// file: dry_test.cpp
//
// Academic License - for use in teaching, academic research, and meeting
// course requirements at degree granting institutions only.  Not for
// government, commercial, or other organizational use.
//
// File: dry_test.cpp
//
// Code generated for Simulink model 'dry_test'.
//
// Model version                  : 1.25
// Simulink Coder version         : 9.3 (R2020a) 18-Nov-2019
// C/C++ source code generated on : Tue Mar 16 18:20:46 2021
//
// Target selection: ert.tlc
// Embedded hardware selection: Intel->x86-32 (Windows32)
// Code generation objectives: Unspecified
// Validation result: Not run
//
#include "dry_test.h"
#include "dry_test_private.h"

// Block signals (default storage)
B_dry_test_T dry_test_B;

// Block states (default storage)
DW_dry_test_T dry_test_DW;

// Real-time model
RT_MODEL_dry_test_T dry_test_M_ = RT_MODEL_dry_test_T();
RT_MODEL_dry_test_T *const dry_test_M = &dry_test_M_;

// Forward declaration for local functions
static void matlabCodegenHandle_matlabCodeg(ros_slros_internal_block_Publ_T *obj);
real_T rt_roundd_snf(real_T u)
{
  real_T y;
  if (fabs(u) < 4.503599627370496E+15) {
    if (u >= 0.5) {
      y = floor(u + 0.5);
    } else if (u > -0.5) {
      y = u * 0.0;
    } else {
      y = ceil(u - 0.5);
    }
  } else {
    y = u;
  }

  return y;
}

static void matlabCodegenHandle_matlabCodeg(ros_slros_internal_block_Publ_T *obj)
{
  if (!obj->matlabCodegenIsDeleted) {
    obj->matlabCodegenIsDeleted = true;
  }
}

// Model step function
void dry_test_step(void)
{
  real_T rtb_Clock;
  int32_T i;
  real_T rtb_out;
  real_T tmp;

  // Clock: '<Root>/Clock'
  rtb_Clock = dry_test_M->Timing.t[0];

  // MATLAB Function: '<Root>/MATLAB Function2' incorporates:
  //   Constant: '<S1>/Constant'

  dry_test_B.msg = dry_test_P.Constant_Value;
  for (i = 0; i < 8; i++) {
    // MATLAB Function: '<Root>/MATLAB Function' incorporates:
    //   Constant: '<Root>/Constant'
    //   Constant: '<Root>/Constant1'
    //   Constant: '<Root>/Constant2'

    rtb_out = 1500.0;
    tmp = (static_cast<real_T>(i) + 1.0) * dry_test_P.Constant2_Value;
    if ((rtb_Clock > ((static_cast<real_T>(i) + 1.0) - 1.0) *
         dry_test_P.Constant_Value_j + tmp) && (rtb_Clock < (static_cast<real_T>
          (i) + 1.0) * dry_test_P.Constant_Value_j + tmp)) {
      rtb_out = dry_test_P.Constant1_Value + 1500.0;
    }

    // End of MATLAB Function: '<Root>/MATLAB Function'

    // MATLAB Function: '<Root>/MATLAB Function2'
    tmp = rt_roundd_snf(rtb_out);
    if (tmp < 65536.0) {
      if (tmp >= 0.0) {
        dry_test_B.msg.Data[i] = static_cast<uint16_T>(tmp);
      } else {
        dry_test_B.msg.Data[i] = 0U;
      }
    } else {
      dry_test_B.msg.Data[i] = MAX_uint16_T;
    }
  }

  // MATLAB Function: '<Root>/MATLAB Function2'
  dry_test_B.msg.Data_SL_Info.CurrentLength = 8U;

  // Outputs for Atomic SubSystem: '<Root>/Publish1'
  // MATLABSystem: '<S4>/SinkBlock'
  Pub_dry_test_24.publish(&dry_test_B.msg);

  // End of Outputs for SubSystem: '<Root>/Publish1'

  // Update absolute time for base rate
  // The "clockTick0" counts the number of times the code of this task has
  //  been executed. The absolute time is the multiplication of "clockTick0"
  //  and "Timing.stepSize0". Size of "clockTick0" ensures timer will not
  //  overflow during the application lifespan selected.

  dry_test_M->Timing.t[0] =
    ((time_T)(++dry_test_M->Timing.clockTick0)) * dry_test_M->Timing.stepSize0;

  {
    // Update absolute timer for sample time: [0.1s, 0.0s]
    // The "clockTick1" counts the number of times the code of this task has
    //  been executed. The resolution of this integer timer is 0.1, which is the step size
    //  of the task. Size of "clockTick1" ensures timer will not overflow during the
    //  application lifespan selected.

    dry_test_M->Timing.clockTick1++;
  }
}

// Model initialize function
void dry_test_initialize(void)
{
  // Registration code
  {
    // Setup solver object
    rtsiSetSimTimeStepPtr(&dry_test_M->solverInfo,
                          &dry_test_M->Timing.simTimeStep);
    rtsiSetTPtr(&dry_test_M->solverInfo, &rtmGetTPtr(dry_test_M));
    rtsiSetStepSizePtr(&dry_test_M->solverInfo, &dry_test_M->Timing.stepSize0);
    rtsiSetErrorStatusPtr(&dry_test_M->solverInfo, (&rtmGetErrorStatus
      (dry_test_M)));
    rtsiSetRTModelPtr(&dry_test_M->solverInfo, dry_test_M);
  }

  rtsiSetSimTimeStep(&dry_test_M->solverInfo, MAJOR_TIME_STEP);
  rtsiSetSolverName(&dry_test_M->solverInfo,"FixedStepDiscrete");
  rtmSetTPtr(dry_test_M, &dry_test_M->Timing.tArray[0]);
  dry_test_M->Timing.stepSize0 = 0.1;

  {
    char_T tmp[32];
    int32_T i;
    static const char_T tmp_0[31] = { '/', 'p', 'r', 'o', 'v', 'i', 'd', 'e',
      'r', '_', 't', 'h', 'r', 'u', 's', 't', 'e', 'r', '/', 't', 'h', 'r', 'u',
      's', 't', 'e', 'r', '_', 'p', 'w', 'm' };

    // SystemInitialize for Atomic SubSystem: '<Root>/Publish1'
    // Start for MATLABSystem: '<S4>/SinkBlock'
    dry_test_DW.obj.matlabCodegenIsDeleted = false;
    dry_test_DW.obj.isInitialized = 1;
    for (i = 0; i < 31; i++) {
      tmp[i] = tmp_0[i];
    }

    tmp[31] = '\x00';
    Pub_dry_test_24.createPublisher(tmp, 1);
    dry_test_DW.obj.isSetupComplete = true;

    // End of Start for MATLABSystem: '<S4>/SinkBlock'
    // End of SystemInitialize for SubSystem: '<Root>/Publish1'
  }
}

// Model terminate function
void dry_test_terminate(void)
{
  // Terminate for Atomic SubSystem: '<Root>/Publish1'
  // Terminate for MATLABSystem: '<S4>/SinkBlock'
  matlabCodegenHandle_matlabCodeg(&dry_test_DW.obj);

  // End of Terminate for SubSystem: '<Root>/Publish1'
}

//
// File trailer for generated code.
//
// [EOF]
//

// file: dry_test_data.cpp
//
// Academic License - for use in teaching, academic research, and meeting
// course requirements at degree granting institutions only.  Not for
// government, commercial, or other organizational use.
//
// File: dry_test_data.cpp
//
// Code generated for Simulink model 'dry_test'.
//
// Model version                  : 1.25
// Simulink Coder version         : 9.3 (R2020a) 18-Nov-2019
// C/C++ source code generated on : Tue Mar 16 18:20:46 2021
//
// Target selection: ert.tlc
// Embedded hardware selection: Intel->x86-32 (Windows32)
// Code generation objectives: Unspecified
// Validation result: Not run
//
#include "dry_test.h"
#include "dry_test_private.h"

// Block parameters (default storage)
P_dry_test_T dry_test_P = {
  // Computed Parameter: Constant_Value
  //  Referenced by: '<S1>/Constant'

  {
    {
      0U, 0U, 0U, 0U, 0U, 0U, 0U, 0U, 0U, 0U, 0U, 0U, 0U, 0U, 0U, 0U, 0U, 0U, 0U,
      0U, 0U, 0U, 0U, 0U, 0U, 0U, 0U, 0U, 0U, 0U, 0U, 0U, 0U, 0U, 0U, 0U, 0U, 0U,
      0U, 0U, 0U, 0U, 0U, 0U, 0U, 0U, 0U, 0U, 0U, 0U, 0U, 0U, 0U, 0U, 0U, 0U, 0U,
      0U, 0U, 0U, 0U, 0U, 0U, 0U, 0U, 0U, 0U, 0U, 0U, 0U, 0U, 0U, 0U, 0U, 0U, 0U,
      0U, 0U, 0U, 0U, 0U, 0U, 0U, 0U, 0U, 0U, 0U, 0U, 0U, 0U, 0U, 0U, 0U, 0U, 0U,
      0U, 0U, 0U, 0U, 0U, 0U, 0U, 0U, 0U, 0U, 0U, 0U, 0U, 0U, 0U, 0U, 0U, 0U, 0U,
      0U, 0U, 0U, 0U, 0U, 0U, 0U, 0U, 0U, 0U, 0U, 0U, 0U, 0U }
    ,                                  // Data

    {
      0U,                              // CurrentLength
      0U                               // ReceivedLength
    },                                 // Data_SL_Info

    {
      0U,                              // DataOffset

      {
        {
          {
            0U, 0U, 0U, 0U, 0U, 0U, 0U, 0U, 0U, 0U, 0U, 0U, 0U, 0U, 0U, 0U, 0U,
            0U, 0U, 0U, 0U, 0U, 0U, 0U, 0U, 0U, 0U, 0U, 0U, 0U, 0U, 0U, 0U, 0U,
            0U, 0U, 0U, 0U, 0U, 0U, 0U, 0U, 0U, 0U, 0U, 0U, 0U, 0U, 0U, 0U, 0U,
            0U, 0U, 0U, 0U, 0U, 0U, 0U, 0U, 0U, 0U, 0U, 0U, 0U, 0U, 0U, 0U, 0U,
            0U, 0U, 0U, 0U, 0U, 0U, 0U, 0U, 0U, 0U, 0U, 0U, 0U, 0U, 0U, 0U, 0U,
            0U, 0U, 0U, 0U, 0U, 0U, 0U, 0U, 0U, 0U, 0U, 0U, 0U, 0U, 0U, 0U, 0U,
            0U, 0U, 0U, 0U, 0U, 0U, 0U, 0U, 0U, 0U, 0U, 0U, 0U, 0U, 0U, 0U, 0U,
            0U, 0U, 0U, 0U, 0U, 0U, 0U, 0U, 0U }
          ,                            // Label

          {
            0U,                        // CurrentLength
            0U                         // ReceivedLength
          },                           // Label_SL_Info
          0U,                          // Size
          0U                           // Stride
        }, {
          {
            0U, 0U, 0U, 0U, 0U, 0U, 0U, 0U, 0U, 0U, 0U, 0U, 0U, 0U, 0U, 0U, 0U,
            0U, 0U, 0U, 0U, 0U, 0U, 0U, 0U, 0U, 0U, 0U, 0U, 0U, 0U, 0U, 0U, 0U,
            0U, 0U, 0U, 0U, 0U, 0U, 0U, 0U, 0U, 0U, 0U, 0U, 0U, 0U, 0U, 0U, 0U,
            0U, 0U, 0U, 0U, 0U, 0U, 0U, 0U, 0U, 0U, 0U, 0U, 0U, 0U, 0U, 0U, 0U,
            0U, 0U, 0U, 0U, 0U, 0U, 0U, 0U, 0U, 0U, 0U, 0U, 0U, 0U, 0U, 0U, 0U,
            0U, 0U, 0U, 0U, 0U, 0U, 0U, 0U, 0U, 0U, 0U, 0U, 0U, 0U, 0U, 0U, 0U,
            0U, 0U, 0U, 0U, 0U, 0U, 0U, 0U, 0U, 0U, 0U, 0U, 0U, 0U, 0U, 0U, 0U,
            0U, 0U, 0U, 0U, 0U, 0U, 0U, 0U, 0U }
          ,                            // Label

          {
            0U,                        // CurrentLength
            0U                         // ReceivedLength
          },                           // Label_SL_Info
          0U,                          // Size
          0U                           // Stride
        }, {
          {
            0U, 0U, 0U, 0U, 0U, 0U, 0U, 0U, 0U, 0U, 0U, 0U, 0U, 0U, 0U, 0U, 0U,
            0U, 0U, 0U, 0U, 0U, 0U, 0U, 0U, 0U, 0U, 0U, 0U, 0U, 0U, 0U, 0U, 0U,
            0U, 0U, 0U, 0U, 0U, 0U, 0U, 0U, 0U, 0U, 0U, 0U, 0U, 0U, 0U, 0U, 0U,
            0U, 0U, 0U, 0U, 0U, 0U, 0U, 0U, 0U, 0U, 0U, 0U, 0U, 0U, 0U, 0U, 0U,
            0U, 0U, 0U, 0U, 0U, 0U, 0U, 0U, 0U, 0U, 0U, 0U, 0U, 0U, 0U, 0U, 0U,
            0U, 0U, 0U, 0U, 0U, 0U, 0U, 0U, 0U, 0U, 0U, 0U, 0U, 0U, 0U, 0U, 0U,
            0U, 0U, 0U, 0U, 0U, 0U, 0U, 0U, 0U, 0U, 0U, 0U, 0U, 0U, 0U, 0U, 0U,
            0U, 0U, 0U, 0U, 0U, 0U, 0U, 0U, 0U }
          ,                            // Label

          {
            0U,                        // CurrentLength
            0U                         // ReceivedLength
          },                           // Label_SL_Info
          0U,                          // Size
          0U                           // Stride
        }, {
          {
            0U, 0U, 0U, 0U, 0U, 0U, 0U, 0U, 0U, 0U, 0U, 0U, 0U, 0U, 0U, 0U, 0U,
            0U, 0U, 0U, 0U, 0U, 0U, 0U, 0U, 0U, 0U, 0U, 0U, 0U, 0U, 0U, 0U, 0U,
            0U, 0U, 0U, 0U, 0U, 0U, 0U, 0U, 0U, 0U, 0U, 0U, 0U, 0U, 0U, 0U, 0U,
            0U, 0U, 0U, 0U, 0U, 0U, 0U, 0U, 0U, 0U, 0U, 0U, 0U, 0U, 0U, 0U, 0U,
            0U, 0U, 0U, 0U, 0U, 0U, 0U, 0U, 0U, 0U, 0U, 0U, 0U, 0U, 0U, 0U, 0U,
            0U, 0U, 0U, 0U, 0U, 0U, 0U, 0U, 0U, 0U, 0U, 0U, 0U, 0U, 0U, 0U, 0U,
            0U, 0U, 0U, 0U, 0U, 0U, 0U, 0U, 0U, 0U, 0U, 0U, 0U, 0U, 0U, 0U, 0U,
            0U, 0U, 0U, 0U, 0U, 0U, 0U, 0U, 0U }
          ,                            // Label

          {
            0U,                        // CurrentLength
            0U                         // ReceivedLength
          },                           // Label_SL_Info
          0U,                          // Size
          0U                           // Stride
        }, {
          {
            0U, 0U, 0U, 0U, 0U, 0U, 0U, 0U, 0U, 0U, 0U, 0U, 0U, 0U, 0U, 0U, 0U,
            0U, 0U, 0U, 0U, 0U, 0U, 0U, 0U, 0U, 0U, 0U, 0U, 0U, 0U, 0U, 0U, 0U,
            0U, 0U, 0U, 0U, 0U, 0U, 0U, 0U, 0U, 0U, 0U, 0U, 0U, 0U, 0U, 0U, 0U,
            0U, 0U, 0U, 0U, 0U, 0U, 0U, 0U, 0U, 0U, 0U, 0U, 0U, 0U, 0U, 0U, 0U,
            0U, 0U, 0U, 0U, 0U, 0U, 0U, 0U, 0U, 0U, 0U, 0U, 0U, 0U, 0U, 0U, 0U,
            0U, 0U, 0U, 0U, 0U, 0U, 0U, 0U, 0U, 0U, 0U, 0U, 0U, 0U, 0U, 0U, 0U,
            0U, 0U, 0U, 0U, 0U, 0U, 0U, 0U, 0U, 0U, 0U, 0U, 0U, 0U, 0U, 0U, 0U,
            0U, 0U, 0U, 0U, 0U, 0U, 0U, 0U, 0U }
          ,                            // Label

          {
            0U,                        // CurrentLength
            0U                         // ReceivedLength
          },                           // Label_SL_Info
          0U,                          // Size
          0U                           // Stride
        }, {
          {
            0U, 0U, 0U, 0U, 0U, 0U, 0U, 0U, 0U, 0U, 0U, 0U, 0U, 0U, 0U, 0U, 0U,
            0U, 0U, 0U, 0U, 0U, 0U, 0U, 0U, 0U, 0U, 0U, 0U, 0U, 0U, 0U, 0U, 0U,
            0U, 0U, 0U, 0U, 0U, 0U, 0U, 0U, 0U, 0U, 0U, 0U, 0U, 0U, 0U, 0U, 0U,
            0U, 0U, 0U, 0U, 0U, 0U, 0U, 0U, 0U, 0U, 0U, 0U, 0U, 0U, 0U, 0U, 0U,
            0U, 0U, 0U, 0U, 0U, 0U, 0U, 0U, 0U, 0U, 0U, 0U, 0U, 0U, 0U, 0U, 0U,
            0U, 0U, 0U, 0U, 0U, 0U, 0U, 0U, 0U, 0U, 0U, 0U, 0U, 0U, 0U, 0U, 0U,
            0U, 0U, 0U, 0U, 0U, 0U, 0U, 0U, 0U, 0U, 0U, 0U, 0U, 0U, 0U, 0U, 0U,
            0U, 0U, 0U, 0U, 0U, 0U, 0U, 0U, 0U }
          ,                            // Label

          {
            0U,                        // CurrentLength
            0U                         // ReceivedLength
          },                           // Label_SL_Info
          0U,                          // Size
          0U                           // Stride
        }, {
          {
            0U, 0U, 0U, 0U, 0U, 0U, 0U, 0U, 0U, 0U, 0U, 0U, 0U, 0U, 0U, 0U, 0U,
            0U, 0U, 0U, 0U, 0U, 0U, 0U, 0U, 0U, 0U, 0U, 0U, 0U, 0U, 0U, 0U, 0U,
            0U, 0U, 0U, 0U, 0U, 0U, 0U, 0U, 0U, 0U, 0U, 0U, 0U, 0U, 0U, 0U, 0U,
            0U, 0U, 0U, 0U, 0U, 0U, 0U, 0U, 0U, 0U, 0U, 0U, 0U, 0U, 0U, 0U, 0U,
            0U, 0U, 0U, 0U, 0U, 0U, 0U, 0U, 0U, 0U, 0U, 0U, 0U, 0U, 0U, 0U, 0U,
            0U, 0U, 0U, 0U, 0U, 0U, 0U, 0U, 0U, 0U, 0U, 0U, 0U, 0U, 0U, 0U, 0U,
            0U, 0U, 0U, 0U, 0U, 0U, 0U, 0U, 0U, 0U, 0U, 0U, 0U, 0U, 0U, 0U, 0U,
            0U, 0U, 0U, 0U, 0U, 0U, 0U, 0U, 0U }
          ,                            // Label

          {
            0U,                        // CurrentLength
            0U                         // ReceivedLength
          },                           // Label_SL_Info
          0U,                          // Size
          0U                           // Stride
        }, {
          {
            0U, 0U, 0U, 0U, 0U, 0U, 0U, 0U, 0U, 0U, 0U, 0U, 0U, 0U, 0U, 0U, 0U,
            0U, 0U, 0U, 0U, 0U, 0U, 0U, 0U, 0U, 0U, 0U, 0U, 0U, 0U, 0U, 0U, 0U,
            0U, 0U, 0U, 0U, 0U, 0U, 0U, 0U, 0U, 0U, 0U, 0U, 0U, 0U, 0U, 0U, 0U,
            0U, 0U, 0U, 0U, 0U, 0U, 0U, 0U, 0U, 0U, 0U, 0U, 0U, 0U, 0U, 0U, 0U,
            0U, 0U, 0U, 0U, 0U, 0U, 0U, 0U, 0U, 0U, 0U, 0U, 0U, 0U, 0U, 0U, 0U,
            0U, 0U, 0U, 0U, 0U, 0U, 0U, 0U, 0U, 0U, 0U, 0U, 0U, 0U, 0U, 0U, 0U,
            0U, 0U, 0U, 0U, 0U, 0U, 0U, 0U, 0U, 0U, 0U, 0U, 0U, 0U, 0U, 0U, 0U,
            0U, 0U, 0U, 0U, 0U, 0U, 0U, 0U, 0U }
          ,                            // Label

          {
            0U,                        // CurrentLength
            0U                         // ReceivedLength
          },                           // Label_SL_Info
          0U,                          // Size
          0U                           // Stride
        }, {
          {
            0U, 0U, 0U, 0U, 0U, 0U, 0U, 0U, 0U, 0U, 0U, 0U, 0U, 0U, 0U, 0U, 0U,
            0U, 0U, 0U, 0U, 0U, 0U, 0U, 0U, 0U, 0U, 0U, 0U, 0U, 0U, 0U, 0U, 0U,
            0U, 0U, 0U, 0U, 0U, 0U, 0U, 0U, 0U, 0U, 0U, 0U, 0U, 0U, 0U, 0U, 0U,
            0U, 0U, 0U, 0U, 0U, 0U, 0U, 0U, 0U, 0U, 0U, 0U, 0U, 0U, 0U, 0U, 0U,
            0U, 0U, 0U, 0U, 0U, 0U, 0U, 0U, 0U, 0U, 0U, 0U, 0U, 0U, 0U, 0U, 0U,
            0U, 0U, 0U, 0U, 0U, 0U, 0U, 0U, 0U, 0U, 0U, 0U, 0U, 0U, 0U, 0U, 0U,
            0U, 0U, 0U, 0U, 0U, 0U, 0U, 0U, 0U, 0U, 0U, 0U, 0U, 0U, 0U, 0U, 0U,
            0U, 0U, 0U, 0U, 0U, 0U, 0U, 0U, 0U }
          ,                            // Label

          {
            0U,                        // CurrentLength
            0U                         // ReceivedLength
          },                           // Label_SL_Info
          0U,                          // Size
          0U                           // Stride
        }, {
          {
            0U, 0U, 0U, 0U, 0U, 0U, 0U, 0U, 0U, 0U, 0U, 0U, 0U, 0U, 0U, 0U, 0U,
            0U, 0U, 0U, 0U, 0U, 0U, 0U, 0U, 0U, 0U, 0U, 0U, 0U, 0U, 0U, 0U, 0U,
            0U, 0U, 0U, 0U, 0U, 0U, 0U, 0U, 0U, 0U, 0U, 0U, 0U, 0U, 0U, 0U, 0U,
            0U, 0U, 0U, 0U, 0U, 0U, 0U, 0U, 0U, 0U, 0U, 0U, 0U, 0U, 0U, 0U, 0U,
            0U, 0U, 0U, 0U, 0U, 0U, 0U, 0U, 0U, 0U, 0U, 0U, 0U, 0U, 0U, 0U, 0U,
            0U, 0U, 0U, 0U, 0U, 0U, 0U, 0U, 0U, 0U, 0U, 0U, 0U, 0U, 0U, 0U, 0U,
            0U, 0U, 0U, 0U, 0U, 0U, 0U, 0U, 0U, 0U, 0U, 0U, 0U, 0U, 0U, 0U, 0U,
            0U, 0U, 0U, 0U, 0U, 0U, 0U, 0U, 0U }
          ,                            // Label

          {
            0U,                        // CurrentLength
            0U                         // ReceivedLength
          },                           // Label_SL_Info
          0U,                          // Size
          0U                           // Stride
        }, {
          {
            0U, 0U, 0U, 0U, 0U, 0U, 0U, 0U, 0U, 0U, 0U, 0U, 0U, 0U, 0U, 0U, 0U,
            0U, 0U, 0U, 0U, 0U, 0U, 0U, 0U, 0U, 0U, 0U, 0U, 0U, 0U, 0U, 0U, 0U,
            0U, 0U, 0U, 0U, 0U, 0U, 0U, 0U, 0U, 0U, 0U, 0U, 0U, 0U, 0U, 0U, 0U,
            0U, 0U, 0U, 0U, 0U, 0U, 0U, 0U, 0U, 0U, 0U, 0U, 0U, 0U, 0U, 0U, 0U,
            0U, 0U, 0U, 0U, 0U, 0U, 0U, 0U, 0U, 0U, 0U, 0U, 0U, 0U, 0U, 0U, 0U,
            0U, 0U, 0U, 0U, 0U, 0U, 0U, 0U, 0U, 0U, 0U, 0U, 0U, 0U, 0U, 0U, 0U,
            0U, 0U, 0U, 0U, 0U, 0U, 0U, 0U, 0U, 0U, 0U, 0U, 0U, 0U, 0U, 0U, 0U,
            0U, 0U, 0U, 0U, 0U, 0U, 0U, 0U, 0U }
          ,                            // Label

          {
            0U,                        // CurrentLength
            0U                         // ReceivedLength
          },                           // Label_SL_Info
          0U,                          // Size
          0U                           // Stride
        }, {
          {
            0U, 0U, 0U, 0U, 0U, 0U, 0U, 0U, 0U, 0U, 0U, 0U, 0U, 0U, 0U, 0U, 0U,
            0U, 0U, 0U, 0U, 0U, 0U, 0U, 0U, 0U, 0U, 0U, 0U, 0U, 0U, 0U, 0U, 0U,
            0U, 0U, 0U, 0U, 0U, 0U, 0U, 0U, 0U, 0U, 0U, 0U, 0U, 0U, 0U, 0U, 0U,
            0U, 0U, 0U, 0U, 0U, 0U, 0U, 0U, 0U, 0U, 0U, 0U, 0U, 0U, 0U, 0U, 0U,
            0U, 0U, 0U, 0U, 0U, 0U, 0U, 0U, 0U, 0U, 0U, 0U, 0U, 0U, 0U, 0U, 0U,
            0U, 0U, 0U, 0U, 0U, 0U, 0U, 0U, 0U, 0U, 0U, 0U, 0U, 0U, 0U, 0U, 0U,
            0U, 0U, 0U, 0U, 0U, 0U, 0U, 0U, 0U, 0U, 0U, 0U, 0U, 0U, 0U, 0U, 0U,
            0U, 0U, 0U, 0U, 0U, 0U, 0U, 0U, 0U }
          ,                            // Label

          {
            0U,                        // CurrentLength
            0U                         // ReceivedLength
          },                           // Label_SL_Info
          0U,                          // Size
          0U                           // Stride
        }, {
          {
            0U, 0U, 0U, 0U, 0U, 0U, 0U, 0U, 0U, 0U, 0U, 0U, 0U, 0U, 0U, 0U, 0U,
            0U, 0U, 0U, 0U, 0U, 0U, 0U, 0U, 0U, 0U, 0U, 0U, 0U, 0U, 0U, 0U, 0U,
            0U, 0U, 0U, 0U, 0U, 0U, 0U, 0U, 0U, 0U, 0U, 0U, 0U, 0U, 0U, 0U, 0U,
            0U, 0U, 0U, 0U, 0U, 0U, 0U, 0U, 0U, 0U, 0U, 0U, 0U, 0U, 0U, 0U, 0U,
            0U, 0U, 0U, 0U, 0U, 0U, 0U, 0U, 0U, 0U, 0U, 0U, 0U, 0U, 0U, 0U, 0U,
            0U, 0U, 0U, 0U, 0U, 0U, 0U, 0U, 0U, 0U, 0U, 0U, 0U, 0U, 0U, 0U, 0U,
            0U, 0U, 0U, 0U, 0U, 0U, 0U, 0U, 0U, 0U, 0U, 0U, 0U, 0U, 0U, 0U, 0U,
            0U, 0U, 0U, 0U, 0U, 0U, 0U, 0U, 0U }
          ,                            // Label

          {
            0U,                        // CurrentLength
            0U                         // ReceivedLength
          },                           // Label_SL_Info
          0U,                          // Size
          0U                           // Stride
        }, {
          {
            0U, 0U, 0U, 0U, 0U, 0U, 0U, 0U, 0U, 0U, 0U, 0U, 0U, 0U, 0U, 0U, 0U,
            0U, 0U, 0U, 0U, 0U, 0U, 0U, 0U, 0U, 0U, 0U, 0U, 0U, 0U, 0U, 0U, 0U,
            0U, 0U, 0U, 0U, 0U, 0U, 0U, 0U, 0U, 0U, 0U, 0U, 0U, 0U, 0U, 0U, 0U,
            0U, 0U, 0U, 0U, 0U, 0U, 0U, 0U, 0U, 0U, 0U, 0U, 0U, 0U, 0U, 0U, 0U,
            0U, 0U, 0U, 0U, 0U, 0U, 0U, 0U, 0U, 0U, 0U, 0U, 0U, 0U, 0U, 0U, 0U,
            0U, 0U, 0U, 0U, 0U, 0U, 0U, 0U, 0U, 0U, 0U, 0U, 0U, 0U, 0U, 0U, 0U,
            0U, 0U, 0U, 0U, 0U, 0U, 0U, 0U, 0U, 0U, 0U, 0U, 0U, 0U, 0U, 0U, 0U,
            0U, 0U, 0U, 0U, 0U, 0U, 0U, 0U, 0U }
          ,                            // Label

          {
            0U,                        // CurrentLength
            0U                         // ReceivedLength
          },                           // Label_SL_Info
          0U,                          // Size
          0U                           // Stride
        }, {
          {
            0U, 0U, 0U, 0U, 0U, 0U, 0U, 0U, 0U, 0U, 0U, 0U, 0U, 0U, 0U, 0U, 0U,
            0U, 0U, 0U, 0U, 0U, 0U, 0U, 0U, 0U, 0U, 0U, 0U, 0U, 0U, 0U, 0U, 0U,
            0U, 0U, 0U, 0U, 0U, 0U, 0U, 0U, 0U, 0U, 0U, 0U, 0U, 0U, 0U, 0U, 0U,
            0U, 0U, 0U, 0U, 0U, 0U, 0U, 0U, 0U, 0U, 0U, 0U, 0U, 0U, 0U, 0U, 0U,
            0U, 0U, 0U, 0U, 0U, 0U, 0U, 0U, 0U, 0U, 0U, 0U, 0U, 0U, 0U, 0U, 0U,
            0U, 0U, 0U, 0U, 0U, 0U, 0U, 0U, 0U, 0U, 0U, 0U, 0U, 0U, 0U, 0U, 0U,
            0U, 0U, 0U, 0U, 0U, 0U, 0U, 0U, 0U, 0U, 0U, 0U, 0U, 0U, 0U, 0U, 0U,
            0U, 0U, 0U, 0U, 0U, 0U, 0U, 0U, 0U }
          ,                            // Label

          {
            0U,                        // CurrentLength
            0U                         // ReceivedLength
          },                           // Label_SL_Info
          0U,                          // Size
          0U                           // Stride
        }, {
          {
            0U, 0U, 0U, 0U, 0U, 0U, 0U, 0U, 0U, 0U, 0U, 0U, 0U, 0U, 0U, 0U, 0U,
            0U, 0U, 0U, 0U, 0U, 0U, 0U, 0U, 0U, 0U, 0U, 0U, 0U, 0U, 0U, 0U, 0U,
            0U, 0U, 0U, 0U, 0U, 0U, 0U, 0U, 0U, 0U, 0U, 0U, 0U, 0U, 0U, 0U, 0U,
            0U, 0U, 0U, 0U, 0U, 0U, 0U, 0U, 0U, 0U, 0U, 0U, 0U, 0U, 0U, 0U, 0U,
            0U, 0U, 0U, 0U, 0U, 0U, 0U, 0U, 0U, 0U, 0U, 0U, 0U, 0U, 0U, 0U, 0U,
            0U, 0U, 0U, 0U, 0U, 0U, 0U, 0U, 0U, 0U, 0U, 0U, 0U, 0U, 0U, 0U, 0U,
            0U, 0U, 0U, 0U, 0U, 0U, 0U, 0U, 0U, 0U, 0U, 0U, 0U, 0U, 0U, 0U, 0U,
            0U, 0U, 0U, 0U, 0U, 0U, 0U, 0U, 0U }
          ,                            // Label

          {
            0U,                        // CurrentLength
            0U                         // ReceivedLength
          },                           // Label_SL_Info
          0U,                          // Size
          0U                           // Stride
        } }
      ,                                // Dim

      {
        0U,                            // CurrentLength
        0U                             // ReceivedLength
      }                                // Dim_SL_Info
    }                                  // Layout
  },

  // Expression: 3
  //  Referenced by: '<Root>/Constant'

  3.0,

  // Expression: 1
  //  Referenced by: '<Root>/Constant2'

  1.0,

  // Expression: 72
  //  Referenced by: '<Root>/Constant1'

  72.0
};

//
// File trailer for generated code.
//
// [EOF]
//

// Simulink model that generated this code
simulink model "dry_test"  (R2020a)
settings: Solver=FixedStepAuto  StartTime=0.0  StopTime=40  FixedStep=.1  RelTol=1e-3
libraries: robotlib x2

== system dry_test ==
  Blank Message1 : robotlib/Blank Message  messageClass=Message  entityType=std_msgs/UInt16MultiArray  messageType=std_msgs/UInt16MultiArray  SampleTime=inf
  Clock : Clock
  Constant : Constant  Value=3
  Constant1 : Constant  Value=72
  Constant2 : Constant
  MATLAB Function : MATLAB Function  TreatAsAtomicUnit=on
  MATLAB Function2 : MATLAB Function  TreatAsAtomicUnit=on
  Publish1 : robotlib/Publish  topicSource=Specify your own  topic=/provider_thruster/thruster_pwm  messageType=std_msgs/UInt16MultiArray  messageQueueLength=1
  Scope : Scope
  wires:
  Constant/1 -> MATLAB Function/2(ontime)
  Clock/1 -> MATLAB Function/1(time)
  Constant1/1 -> MATLAB Function/4(command)
  Constant2/1 -> MATLAB Function/3(delay)
  MATLAB Function2/1(msg) -> Publish1/1
  MATLAB Function/1(out) -> MATLAB Function2/2(pwm), Scope/1
  Blank Message1/1 -> MATLAB Function2/1(blankMsg)

== matlab function dry_test/MATLAB Function ==
function out = DryTest(time, ontime,delay, command)
out=repmat(1500,8,1);
for i=1:8
    if time>ontime*(i-1)+((i)*delay) && time<ontime*(i)+(i*delay)
       out(i)= out(i)+command;
    end
end

== matlab function dry_test/MATLAB Function2 ==
function msg = assignThrusterPwm(blankMsg, pwm)
msg = blankMsg;
msg.Data(1:8) = cast(pwm, 'uint16');
msg.Data_SL_Info.CurrentLength = uint32(8);
